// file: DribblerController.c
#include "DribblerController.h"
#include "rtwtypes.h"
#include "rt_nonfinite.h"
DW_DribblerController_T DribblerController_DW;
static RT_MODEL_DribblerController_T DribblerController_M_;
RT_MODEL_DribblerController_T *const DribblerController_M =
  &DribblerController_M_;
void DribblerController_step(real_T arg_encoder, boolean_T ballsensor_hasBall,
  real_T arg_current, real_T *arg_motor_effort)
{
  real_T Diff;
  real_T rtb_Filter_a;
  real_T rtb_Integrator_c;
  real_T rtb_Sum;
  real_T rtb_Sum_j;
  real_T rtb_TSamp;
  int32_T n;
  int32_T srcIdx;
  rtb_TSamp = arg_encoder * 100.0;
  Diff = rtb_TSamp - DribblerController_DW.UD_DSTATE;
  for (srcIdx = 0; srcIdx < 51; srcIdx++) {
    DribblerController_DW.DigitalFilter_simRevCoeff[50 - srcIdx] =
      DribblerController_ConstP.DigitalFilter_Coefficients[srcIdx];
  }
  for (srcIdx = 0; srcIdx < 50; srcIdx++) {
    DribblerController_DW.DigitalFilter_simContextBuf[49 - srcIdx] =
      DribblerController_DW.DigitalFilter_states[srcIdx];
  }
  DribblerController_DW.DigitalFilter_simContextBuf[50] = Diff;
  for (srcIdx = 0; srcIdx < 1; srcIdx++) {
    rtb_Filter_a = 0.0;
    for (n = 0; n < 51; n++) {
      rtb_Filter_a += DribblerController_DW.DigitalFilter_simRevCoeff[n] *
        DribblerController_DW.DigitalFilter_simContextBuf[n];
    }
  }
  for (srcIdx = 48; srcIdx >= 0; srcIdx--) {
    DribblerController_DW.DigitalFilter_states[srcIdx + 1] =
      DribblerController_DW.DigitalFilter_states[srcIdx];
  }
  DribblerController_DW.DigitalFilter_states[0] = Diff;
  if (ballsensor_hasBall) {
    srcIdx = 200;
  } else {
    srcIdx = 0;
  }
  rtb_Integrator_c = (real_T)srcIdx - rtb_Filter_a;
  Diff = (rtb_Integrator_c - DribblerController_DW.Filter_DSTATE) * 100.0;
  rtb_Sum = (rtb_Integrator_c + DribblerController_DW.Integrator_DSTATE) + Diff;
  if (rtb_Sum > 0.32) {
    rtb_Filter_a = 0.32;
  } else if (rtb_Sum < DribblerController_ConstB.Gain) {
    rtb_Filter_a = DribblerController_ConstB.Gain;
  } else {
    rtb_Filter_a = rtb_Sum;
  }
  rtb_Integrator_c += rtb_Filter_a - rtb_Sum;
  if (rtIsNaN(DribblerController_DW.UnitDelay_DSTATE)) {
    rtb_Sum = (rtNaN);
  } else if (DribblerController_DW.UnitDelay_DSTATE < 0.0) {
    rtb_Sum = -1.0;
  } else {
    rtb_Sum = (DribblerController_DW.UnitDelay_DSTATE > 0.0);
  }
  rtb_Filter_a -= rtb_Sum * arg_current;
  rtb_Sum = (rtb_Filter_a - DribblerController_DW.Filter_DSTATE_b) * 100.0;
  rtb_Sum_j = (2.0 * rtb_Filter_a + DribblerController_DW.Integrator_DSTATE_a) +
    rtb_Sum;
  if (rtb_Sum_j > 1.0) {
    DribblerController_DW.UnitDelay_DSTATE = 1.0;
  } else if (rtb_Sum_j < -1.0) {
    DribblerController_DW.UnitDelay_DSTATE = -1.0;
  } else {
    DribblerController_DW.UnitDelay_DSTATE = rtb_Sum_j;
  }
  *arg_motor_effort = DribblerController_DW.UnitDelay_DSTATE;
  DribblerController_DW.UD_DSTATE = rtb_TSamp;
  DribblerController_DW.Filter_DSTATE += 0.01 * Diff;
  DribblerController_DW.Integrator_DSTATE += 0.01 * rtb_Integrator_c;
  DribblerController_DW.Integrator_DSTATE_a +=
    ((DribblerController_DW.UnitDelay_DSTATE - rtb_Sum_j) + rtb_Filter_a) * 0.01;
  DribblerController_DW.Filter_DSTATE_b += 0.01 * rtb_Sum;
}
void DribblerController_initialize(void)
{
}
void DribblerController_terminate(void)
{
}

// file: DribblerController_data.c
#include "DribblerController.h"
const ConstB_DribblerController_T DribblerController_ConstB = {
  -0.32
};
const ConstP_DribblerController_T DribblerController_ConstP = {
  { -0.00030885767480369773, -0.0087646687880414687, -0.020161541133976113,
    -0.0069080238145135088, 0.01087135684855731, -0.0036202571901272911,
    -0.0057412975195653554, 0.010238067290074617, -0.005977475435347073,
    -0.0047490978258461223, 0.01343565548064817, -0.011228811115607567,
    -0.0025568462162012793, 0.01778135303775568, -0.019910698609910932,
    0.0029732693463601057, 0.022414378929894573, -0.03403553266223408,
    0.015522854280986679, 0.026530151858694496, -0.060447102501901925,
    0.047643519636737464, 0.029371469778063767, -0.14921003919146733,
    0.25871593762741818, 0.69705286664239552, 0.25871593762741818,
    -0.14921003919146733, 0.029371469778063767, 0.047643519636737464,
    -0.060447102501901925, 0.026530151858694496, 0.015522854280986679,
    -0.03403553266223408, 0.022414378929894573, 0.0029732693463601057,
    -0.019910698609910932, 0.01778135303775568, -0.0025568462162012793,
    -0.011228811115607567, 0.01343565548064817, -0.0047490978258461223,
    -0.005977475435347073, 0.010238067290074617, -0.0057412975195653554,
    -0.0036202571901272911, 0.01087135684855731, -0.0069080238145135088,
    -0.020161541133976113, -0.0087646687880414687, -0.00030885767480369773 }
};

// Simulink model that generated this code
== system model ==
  encoder : Inport
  Inport#1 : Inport
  current : Inport
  motor_effort : Outport  <- 1: PIDController#1
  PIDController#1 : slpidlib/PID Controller  Controller=PID  Form=Parallel  TimeDomain=Discrete-time  IntegratorMethod=Forward Euler  P=2  I=1  D=1  N=100  InitialConditionForIntegrator=0  ExternalReset=none  LimitOutput=on  UpperSaturationLimit=1  LowerSaturationLimit=-1  <- 1: Sum#1
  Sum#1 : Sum  Inputs=+-  <- 1: PIDController#2, 2: Product#1
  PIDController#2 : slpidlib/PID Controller  Controller=PID  Form=Parallel  TimeDomain=Discrete-time  IntegratorMethod=Forward Euler  P=1  I=1  D=1  N=100  InitialConditionForIntegrator=0  ExternalReset=none  LimitOutput=on  UpperSaturationLimit=inf  LowerSaturationLimit=-inf  <- 1: Sum, 2: Constant#1, 3: Gain
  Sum : Sum  Inputs=+-  <- 1: Switch#1, 2: DigitalFilterDesign#1
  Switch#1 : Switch  Criteria=u2 > Threshold  <- 1: Constant#2, 2: Inport#1, 3: Constant#3
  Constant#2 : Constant  Value=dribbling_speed
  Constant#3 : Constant  Value=0
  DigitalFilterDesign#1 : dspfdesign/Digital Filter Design  <- 1: DiscreteDerivative#1
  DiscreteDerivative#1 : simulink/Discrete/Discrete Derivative  gainval=1.0  <- 1: encoder
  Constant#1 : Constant  Value=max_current
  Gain : Gain  Gain=-1  <- 1: Constant#1
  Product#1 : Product  <- 1: Signum#1, 2: current
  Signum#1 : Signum  <- 1: UnitDelay
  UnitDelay : UnitDelay  <- 1: PIDController#1
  ObserverReference#1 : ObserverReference
